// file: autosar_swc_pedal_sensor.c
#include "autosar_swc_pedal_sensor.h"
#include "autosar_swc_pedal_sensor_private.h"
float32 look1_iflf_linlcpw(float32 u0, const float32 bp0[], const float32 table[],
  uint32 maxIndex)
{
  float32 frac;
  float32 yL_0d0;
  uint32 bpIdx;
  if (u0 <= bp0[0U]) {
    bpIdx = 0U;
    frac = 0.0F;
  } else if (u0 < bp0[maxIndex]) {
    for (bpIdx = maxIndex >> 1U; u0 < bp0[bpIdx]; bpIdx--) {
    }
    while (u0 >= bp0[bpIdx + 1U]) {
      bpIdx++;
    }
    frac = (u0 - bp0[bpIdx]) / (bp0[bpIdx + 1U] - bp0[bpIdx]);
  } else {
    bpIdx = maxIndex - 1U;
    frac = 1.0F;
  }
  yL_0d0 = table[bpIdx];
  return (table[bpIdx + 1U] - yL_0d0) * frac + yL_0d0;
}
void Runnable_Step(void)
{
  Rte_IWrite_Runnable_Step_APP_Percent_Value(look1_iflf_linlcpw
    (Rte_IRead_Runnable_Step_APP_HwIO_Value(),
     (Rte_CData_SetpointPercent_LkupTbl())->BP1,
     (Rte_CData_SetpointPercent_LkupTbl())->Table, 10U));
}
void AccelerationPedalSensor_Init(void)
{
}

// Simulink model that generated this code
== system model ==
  APP_HwIO_Value : Inport
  APP_Percent_Value : Outport  <- 1: Subsystem#1
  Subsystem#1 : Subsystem  <- 1: APP_HwIO_Value
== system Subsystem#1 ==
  Inport#1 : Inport
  Outport#1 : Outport  <- 1: Lookup_nD#1
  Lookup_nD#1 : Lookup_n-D  BreakpointsForDimension1=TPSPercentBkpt  Table=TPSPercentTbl  <- 1: DataTypeConversion#1
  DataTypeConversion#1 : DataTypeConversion  <- 1: Inport#1
